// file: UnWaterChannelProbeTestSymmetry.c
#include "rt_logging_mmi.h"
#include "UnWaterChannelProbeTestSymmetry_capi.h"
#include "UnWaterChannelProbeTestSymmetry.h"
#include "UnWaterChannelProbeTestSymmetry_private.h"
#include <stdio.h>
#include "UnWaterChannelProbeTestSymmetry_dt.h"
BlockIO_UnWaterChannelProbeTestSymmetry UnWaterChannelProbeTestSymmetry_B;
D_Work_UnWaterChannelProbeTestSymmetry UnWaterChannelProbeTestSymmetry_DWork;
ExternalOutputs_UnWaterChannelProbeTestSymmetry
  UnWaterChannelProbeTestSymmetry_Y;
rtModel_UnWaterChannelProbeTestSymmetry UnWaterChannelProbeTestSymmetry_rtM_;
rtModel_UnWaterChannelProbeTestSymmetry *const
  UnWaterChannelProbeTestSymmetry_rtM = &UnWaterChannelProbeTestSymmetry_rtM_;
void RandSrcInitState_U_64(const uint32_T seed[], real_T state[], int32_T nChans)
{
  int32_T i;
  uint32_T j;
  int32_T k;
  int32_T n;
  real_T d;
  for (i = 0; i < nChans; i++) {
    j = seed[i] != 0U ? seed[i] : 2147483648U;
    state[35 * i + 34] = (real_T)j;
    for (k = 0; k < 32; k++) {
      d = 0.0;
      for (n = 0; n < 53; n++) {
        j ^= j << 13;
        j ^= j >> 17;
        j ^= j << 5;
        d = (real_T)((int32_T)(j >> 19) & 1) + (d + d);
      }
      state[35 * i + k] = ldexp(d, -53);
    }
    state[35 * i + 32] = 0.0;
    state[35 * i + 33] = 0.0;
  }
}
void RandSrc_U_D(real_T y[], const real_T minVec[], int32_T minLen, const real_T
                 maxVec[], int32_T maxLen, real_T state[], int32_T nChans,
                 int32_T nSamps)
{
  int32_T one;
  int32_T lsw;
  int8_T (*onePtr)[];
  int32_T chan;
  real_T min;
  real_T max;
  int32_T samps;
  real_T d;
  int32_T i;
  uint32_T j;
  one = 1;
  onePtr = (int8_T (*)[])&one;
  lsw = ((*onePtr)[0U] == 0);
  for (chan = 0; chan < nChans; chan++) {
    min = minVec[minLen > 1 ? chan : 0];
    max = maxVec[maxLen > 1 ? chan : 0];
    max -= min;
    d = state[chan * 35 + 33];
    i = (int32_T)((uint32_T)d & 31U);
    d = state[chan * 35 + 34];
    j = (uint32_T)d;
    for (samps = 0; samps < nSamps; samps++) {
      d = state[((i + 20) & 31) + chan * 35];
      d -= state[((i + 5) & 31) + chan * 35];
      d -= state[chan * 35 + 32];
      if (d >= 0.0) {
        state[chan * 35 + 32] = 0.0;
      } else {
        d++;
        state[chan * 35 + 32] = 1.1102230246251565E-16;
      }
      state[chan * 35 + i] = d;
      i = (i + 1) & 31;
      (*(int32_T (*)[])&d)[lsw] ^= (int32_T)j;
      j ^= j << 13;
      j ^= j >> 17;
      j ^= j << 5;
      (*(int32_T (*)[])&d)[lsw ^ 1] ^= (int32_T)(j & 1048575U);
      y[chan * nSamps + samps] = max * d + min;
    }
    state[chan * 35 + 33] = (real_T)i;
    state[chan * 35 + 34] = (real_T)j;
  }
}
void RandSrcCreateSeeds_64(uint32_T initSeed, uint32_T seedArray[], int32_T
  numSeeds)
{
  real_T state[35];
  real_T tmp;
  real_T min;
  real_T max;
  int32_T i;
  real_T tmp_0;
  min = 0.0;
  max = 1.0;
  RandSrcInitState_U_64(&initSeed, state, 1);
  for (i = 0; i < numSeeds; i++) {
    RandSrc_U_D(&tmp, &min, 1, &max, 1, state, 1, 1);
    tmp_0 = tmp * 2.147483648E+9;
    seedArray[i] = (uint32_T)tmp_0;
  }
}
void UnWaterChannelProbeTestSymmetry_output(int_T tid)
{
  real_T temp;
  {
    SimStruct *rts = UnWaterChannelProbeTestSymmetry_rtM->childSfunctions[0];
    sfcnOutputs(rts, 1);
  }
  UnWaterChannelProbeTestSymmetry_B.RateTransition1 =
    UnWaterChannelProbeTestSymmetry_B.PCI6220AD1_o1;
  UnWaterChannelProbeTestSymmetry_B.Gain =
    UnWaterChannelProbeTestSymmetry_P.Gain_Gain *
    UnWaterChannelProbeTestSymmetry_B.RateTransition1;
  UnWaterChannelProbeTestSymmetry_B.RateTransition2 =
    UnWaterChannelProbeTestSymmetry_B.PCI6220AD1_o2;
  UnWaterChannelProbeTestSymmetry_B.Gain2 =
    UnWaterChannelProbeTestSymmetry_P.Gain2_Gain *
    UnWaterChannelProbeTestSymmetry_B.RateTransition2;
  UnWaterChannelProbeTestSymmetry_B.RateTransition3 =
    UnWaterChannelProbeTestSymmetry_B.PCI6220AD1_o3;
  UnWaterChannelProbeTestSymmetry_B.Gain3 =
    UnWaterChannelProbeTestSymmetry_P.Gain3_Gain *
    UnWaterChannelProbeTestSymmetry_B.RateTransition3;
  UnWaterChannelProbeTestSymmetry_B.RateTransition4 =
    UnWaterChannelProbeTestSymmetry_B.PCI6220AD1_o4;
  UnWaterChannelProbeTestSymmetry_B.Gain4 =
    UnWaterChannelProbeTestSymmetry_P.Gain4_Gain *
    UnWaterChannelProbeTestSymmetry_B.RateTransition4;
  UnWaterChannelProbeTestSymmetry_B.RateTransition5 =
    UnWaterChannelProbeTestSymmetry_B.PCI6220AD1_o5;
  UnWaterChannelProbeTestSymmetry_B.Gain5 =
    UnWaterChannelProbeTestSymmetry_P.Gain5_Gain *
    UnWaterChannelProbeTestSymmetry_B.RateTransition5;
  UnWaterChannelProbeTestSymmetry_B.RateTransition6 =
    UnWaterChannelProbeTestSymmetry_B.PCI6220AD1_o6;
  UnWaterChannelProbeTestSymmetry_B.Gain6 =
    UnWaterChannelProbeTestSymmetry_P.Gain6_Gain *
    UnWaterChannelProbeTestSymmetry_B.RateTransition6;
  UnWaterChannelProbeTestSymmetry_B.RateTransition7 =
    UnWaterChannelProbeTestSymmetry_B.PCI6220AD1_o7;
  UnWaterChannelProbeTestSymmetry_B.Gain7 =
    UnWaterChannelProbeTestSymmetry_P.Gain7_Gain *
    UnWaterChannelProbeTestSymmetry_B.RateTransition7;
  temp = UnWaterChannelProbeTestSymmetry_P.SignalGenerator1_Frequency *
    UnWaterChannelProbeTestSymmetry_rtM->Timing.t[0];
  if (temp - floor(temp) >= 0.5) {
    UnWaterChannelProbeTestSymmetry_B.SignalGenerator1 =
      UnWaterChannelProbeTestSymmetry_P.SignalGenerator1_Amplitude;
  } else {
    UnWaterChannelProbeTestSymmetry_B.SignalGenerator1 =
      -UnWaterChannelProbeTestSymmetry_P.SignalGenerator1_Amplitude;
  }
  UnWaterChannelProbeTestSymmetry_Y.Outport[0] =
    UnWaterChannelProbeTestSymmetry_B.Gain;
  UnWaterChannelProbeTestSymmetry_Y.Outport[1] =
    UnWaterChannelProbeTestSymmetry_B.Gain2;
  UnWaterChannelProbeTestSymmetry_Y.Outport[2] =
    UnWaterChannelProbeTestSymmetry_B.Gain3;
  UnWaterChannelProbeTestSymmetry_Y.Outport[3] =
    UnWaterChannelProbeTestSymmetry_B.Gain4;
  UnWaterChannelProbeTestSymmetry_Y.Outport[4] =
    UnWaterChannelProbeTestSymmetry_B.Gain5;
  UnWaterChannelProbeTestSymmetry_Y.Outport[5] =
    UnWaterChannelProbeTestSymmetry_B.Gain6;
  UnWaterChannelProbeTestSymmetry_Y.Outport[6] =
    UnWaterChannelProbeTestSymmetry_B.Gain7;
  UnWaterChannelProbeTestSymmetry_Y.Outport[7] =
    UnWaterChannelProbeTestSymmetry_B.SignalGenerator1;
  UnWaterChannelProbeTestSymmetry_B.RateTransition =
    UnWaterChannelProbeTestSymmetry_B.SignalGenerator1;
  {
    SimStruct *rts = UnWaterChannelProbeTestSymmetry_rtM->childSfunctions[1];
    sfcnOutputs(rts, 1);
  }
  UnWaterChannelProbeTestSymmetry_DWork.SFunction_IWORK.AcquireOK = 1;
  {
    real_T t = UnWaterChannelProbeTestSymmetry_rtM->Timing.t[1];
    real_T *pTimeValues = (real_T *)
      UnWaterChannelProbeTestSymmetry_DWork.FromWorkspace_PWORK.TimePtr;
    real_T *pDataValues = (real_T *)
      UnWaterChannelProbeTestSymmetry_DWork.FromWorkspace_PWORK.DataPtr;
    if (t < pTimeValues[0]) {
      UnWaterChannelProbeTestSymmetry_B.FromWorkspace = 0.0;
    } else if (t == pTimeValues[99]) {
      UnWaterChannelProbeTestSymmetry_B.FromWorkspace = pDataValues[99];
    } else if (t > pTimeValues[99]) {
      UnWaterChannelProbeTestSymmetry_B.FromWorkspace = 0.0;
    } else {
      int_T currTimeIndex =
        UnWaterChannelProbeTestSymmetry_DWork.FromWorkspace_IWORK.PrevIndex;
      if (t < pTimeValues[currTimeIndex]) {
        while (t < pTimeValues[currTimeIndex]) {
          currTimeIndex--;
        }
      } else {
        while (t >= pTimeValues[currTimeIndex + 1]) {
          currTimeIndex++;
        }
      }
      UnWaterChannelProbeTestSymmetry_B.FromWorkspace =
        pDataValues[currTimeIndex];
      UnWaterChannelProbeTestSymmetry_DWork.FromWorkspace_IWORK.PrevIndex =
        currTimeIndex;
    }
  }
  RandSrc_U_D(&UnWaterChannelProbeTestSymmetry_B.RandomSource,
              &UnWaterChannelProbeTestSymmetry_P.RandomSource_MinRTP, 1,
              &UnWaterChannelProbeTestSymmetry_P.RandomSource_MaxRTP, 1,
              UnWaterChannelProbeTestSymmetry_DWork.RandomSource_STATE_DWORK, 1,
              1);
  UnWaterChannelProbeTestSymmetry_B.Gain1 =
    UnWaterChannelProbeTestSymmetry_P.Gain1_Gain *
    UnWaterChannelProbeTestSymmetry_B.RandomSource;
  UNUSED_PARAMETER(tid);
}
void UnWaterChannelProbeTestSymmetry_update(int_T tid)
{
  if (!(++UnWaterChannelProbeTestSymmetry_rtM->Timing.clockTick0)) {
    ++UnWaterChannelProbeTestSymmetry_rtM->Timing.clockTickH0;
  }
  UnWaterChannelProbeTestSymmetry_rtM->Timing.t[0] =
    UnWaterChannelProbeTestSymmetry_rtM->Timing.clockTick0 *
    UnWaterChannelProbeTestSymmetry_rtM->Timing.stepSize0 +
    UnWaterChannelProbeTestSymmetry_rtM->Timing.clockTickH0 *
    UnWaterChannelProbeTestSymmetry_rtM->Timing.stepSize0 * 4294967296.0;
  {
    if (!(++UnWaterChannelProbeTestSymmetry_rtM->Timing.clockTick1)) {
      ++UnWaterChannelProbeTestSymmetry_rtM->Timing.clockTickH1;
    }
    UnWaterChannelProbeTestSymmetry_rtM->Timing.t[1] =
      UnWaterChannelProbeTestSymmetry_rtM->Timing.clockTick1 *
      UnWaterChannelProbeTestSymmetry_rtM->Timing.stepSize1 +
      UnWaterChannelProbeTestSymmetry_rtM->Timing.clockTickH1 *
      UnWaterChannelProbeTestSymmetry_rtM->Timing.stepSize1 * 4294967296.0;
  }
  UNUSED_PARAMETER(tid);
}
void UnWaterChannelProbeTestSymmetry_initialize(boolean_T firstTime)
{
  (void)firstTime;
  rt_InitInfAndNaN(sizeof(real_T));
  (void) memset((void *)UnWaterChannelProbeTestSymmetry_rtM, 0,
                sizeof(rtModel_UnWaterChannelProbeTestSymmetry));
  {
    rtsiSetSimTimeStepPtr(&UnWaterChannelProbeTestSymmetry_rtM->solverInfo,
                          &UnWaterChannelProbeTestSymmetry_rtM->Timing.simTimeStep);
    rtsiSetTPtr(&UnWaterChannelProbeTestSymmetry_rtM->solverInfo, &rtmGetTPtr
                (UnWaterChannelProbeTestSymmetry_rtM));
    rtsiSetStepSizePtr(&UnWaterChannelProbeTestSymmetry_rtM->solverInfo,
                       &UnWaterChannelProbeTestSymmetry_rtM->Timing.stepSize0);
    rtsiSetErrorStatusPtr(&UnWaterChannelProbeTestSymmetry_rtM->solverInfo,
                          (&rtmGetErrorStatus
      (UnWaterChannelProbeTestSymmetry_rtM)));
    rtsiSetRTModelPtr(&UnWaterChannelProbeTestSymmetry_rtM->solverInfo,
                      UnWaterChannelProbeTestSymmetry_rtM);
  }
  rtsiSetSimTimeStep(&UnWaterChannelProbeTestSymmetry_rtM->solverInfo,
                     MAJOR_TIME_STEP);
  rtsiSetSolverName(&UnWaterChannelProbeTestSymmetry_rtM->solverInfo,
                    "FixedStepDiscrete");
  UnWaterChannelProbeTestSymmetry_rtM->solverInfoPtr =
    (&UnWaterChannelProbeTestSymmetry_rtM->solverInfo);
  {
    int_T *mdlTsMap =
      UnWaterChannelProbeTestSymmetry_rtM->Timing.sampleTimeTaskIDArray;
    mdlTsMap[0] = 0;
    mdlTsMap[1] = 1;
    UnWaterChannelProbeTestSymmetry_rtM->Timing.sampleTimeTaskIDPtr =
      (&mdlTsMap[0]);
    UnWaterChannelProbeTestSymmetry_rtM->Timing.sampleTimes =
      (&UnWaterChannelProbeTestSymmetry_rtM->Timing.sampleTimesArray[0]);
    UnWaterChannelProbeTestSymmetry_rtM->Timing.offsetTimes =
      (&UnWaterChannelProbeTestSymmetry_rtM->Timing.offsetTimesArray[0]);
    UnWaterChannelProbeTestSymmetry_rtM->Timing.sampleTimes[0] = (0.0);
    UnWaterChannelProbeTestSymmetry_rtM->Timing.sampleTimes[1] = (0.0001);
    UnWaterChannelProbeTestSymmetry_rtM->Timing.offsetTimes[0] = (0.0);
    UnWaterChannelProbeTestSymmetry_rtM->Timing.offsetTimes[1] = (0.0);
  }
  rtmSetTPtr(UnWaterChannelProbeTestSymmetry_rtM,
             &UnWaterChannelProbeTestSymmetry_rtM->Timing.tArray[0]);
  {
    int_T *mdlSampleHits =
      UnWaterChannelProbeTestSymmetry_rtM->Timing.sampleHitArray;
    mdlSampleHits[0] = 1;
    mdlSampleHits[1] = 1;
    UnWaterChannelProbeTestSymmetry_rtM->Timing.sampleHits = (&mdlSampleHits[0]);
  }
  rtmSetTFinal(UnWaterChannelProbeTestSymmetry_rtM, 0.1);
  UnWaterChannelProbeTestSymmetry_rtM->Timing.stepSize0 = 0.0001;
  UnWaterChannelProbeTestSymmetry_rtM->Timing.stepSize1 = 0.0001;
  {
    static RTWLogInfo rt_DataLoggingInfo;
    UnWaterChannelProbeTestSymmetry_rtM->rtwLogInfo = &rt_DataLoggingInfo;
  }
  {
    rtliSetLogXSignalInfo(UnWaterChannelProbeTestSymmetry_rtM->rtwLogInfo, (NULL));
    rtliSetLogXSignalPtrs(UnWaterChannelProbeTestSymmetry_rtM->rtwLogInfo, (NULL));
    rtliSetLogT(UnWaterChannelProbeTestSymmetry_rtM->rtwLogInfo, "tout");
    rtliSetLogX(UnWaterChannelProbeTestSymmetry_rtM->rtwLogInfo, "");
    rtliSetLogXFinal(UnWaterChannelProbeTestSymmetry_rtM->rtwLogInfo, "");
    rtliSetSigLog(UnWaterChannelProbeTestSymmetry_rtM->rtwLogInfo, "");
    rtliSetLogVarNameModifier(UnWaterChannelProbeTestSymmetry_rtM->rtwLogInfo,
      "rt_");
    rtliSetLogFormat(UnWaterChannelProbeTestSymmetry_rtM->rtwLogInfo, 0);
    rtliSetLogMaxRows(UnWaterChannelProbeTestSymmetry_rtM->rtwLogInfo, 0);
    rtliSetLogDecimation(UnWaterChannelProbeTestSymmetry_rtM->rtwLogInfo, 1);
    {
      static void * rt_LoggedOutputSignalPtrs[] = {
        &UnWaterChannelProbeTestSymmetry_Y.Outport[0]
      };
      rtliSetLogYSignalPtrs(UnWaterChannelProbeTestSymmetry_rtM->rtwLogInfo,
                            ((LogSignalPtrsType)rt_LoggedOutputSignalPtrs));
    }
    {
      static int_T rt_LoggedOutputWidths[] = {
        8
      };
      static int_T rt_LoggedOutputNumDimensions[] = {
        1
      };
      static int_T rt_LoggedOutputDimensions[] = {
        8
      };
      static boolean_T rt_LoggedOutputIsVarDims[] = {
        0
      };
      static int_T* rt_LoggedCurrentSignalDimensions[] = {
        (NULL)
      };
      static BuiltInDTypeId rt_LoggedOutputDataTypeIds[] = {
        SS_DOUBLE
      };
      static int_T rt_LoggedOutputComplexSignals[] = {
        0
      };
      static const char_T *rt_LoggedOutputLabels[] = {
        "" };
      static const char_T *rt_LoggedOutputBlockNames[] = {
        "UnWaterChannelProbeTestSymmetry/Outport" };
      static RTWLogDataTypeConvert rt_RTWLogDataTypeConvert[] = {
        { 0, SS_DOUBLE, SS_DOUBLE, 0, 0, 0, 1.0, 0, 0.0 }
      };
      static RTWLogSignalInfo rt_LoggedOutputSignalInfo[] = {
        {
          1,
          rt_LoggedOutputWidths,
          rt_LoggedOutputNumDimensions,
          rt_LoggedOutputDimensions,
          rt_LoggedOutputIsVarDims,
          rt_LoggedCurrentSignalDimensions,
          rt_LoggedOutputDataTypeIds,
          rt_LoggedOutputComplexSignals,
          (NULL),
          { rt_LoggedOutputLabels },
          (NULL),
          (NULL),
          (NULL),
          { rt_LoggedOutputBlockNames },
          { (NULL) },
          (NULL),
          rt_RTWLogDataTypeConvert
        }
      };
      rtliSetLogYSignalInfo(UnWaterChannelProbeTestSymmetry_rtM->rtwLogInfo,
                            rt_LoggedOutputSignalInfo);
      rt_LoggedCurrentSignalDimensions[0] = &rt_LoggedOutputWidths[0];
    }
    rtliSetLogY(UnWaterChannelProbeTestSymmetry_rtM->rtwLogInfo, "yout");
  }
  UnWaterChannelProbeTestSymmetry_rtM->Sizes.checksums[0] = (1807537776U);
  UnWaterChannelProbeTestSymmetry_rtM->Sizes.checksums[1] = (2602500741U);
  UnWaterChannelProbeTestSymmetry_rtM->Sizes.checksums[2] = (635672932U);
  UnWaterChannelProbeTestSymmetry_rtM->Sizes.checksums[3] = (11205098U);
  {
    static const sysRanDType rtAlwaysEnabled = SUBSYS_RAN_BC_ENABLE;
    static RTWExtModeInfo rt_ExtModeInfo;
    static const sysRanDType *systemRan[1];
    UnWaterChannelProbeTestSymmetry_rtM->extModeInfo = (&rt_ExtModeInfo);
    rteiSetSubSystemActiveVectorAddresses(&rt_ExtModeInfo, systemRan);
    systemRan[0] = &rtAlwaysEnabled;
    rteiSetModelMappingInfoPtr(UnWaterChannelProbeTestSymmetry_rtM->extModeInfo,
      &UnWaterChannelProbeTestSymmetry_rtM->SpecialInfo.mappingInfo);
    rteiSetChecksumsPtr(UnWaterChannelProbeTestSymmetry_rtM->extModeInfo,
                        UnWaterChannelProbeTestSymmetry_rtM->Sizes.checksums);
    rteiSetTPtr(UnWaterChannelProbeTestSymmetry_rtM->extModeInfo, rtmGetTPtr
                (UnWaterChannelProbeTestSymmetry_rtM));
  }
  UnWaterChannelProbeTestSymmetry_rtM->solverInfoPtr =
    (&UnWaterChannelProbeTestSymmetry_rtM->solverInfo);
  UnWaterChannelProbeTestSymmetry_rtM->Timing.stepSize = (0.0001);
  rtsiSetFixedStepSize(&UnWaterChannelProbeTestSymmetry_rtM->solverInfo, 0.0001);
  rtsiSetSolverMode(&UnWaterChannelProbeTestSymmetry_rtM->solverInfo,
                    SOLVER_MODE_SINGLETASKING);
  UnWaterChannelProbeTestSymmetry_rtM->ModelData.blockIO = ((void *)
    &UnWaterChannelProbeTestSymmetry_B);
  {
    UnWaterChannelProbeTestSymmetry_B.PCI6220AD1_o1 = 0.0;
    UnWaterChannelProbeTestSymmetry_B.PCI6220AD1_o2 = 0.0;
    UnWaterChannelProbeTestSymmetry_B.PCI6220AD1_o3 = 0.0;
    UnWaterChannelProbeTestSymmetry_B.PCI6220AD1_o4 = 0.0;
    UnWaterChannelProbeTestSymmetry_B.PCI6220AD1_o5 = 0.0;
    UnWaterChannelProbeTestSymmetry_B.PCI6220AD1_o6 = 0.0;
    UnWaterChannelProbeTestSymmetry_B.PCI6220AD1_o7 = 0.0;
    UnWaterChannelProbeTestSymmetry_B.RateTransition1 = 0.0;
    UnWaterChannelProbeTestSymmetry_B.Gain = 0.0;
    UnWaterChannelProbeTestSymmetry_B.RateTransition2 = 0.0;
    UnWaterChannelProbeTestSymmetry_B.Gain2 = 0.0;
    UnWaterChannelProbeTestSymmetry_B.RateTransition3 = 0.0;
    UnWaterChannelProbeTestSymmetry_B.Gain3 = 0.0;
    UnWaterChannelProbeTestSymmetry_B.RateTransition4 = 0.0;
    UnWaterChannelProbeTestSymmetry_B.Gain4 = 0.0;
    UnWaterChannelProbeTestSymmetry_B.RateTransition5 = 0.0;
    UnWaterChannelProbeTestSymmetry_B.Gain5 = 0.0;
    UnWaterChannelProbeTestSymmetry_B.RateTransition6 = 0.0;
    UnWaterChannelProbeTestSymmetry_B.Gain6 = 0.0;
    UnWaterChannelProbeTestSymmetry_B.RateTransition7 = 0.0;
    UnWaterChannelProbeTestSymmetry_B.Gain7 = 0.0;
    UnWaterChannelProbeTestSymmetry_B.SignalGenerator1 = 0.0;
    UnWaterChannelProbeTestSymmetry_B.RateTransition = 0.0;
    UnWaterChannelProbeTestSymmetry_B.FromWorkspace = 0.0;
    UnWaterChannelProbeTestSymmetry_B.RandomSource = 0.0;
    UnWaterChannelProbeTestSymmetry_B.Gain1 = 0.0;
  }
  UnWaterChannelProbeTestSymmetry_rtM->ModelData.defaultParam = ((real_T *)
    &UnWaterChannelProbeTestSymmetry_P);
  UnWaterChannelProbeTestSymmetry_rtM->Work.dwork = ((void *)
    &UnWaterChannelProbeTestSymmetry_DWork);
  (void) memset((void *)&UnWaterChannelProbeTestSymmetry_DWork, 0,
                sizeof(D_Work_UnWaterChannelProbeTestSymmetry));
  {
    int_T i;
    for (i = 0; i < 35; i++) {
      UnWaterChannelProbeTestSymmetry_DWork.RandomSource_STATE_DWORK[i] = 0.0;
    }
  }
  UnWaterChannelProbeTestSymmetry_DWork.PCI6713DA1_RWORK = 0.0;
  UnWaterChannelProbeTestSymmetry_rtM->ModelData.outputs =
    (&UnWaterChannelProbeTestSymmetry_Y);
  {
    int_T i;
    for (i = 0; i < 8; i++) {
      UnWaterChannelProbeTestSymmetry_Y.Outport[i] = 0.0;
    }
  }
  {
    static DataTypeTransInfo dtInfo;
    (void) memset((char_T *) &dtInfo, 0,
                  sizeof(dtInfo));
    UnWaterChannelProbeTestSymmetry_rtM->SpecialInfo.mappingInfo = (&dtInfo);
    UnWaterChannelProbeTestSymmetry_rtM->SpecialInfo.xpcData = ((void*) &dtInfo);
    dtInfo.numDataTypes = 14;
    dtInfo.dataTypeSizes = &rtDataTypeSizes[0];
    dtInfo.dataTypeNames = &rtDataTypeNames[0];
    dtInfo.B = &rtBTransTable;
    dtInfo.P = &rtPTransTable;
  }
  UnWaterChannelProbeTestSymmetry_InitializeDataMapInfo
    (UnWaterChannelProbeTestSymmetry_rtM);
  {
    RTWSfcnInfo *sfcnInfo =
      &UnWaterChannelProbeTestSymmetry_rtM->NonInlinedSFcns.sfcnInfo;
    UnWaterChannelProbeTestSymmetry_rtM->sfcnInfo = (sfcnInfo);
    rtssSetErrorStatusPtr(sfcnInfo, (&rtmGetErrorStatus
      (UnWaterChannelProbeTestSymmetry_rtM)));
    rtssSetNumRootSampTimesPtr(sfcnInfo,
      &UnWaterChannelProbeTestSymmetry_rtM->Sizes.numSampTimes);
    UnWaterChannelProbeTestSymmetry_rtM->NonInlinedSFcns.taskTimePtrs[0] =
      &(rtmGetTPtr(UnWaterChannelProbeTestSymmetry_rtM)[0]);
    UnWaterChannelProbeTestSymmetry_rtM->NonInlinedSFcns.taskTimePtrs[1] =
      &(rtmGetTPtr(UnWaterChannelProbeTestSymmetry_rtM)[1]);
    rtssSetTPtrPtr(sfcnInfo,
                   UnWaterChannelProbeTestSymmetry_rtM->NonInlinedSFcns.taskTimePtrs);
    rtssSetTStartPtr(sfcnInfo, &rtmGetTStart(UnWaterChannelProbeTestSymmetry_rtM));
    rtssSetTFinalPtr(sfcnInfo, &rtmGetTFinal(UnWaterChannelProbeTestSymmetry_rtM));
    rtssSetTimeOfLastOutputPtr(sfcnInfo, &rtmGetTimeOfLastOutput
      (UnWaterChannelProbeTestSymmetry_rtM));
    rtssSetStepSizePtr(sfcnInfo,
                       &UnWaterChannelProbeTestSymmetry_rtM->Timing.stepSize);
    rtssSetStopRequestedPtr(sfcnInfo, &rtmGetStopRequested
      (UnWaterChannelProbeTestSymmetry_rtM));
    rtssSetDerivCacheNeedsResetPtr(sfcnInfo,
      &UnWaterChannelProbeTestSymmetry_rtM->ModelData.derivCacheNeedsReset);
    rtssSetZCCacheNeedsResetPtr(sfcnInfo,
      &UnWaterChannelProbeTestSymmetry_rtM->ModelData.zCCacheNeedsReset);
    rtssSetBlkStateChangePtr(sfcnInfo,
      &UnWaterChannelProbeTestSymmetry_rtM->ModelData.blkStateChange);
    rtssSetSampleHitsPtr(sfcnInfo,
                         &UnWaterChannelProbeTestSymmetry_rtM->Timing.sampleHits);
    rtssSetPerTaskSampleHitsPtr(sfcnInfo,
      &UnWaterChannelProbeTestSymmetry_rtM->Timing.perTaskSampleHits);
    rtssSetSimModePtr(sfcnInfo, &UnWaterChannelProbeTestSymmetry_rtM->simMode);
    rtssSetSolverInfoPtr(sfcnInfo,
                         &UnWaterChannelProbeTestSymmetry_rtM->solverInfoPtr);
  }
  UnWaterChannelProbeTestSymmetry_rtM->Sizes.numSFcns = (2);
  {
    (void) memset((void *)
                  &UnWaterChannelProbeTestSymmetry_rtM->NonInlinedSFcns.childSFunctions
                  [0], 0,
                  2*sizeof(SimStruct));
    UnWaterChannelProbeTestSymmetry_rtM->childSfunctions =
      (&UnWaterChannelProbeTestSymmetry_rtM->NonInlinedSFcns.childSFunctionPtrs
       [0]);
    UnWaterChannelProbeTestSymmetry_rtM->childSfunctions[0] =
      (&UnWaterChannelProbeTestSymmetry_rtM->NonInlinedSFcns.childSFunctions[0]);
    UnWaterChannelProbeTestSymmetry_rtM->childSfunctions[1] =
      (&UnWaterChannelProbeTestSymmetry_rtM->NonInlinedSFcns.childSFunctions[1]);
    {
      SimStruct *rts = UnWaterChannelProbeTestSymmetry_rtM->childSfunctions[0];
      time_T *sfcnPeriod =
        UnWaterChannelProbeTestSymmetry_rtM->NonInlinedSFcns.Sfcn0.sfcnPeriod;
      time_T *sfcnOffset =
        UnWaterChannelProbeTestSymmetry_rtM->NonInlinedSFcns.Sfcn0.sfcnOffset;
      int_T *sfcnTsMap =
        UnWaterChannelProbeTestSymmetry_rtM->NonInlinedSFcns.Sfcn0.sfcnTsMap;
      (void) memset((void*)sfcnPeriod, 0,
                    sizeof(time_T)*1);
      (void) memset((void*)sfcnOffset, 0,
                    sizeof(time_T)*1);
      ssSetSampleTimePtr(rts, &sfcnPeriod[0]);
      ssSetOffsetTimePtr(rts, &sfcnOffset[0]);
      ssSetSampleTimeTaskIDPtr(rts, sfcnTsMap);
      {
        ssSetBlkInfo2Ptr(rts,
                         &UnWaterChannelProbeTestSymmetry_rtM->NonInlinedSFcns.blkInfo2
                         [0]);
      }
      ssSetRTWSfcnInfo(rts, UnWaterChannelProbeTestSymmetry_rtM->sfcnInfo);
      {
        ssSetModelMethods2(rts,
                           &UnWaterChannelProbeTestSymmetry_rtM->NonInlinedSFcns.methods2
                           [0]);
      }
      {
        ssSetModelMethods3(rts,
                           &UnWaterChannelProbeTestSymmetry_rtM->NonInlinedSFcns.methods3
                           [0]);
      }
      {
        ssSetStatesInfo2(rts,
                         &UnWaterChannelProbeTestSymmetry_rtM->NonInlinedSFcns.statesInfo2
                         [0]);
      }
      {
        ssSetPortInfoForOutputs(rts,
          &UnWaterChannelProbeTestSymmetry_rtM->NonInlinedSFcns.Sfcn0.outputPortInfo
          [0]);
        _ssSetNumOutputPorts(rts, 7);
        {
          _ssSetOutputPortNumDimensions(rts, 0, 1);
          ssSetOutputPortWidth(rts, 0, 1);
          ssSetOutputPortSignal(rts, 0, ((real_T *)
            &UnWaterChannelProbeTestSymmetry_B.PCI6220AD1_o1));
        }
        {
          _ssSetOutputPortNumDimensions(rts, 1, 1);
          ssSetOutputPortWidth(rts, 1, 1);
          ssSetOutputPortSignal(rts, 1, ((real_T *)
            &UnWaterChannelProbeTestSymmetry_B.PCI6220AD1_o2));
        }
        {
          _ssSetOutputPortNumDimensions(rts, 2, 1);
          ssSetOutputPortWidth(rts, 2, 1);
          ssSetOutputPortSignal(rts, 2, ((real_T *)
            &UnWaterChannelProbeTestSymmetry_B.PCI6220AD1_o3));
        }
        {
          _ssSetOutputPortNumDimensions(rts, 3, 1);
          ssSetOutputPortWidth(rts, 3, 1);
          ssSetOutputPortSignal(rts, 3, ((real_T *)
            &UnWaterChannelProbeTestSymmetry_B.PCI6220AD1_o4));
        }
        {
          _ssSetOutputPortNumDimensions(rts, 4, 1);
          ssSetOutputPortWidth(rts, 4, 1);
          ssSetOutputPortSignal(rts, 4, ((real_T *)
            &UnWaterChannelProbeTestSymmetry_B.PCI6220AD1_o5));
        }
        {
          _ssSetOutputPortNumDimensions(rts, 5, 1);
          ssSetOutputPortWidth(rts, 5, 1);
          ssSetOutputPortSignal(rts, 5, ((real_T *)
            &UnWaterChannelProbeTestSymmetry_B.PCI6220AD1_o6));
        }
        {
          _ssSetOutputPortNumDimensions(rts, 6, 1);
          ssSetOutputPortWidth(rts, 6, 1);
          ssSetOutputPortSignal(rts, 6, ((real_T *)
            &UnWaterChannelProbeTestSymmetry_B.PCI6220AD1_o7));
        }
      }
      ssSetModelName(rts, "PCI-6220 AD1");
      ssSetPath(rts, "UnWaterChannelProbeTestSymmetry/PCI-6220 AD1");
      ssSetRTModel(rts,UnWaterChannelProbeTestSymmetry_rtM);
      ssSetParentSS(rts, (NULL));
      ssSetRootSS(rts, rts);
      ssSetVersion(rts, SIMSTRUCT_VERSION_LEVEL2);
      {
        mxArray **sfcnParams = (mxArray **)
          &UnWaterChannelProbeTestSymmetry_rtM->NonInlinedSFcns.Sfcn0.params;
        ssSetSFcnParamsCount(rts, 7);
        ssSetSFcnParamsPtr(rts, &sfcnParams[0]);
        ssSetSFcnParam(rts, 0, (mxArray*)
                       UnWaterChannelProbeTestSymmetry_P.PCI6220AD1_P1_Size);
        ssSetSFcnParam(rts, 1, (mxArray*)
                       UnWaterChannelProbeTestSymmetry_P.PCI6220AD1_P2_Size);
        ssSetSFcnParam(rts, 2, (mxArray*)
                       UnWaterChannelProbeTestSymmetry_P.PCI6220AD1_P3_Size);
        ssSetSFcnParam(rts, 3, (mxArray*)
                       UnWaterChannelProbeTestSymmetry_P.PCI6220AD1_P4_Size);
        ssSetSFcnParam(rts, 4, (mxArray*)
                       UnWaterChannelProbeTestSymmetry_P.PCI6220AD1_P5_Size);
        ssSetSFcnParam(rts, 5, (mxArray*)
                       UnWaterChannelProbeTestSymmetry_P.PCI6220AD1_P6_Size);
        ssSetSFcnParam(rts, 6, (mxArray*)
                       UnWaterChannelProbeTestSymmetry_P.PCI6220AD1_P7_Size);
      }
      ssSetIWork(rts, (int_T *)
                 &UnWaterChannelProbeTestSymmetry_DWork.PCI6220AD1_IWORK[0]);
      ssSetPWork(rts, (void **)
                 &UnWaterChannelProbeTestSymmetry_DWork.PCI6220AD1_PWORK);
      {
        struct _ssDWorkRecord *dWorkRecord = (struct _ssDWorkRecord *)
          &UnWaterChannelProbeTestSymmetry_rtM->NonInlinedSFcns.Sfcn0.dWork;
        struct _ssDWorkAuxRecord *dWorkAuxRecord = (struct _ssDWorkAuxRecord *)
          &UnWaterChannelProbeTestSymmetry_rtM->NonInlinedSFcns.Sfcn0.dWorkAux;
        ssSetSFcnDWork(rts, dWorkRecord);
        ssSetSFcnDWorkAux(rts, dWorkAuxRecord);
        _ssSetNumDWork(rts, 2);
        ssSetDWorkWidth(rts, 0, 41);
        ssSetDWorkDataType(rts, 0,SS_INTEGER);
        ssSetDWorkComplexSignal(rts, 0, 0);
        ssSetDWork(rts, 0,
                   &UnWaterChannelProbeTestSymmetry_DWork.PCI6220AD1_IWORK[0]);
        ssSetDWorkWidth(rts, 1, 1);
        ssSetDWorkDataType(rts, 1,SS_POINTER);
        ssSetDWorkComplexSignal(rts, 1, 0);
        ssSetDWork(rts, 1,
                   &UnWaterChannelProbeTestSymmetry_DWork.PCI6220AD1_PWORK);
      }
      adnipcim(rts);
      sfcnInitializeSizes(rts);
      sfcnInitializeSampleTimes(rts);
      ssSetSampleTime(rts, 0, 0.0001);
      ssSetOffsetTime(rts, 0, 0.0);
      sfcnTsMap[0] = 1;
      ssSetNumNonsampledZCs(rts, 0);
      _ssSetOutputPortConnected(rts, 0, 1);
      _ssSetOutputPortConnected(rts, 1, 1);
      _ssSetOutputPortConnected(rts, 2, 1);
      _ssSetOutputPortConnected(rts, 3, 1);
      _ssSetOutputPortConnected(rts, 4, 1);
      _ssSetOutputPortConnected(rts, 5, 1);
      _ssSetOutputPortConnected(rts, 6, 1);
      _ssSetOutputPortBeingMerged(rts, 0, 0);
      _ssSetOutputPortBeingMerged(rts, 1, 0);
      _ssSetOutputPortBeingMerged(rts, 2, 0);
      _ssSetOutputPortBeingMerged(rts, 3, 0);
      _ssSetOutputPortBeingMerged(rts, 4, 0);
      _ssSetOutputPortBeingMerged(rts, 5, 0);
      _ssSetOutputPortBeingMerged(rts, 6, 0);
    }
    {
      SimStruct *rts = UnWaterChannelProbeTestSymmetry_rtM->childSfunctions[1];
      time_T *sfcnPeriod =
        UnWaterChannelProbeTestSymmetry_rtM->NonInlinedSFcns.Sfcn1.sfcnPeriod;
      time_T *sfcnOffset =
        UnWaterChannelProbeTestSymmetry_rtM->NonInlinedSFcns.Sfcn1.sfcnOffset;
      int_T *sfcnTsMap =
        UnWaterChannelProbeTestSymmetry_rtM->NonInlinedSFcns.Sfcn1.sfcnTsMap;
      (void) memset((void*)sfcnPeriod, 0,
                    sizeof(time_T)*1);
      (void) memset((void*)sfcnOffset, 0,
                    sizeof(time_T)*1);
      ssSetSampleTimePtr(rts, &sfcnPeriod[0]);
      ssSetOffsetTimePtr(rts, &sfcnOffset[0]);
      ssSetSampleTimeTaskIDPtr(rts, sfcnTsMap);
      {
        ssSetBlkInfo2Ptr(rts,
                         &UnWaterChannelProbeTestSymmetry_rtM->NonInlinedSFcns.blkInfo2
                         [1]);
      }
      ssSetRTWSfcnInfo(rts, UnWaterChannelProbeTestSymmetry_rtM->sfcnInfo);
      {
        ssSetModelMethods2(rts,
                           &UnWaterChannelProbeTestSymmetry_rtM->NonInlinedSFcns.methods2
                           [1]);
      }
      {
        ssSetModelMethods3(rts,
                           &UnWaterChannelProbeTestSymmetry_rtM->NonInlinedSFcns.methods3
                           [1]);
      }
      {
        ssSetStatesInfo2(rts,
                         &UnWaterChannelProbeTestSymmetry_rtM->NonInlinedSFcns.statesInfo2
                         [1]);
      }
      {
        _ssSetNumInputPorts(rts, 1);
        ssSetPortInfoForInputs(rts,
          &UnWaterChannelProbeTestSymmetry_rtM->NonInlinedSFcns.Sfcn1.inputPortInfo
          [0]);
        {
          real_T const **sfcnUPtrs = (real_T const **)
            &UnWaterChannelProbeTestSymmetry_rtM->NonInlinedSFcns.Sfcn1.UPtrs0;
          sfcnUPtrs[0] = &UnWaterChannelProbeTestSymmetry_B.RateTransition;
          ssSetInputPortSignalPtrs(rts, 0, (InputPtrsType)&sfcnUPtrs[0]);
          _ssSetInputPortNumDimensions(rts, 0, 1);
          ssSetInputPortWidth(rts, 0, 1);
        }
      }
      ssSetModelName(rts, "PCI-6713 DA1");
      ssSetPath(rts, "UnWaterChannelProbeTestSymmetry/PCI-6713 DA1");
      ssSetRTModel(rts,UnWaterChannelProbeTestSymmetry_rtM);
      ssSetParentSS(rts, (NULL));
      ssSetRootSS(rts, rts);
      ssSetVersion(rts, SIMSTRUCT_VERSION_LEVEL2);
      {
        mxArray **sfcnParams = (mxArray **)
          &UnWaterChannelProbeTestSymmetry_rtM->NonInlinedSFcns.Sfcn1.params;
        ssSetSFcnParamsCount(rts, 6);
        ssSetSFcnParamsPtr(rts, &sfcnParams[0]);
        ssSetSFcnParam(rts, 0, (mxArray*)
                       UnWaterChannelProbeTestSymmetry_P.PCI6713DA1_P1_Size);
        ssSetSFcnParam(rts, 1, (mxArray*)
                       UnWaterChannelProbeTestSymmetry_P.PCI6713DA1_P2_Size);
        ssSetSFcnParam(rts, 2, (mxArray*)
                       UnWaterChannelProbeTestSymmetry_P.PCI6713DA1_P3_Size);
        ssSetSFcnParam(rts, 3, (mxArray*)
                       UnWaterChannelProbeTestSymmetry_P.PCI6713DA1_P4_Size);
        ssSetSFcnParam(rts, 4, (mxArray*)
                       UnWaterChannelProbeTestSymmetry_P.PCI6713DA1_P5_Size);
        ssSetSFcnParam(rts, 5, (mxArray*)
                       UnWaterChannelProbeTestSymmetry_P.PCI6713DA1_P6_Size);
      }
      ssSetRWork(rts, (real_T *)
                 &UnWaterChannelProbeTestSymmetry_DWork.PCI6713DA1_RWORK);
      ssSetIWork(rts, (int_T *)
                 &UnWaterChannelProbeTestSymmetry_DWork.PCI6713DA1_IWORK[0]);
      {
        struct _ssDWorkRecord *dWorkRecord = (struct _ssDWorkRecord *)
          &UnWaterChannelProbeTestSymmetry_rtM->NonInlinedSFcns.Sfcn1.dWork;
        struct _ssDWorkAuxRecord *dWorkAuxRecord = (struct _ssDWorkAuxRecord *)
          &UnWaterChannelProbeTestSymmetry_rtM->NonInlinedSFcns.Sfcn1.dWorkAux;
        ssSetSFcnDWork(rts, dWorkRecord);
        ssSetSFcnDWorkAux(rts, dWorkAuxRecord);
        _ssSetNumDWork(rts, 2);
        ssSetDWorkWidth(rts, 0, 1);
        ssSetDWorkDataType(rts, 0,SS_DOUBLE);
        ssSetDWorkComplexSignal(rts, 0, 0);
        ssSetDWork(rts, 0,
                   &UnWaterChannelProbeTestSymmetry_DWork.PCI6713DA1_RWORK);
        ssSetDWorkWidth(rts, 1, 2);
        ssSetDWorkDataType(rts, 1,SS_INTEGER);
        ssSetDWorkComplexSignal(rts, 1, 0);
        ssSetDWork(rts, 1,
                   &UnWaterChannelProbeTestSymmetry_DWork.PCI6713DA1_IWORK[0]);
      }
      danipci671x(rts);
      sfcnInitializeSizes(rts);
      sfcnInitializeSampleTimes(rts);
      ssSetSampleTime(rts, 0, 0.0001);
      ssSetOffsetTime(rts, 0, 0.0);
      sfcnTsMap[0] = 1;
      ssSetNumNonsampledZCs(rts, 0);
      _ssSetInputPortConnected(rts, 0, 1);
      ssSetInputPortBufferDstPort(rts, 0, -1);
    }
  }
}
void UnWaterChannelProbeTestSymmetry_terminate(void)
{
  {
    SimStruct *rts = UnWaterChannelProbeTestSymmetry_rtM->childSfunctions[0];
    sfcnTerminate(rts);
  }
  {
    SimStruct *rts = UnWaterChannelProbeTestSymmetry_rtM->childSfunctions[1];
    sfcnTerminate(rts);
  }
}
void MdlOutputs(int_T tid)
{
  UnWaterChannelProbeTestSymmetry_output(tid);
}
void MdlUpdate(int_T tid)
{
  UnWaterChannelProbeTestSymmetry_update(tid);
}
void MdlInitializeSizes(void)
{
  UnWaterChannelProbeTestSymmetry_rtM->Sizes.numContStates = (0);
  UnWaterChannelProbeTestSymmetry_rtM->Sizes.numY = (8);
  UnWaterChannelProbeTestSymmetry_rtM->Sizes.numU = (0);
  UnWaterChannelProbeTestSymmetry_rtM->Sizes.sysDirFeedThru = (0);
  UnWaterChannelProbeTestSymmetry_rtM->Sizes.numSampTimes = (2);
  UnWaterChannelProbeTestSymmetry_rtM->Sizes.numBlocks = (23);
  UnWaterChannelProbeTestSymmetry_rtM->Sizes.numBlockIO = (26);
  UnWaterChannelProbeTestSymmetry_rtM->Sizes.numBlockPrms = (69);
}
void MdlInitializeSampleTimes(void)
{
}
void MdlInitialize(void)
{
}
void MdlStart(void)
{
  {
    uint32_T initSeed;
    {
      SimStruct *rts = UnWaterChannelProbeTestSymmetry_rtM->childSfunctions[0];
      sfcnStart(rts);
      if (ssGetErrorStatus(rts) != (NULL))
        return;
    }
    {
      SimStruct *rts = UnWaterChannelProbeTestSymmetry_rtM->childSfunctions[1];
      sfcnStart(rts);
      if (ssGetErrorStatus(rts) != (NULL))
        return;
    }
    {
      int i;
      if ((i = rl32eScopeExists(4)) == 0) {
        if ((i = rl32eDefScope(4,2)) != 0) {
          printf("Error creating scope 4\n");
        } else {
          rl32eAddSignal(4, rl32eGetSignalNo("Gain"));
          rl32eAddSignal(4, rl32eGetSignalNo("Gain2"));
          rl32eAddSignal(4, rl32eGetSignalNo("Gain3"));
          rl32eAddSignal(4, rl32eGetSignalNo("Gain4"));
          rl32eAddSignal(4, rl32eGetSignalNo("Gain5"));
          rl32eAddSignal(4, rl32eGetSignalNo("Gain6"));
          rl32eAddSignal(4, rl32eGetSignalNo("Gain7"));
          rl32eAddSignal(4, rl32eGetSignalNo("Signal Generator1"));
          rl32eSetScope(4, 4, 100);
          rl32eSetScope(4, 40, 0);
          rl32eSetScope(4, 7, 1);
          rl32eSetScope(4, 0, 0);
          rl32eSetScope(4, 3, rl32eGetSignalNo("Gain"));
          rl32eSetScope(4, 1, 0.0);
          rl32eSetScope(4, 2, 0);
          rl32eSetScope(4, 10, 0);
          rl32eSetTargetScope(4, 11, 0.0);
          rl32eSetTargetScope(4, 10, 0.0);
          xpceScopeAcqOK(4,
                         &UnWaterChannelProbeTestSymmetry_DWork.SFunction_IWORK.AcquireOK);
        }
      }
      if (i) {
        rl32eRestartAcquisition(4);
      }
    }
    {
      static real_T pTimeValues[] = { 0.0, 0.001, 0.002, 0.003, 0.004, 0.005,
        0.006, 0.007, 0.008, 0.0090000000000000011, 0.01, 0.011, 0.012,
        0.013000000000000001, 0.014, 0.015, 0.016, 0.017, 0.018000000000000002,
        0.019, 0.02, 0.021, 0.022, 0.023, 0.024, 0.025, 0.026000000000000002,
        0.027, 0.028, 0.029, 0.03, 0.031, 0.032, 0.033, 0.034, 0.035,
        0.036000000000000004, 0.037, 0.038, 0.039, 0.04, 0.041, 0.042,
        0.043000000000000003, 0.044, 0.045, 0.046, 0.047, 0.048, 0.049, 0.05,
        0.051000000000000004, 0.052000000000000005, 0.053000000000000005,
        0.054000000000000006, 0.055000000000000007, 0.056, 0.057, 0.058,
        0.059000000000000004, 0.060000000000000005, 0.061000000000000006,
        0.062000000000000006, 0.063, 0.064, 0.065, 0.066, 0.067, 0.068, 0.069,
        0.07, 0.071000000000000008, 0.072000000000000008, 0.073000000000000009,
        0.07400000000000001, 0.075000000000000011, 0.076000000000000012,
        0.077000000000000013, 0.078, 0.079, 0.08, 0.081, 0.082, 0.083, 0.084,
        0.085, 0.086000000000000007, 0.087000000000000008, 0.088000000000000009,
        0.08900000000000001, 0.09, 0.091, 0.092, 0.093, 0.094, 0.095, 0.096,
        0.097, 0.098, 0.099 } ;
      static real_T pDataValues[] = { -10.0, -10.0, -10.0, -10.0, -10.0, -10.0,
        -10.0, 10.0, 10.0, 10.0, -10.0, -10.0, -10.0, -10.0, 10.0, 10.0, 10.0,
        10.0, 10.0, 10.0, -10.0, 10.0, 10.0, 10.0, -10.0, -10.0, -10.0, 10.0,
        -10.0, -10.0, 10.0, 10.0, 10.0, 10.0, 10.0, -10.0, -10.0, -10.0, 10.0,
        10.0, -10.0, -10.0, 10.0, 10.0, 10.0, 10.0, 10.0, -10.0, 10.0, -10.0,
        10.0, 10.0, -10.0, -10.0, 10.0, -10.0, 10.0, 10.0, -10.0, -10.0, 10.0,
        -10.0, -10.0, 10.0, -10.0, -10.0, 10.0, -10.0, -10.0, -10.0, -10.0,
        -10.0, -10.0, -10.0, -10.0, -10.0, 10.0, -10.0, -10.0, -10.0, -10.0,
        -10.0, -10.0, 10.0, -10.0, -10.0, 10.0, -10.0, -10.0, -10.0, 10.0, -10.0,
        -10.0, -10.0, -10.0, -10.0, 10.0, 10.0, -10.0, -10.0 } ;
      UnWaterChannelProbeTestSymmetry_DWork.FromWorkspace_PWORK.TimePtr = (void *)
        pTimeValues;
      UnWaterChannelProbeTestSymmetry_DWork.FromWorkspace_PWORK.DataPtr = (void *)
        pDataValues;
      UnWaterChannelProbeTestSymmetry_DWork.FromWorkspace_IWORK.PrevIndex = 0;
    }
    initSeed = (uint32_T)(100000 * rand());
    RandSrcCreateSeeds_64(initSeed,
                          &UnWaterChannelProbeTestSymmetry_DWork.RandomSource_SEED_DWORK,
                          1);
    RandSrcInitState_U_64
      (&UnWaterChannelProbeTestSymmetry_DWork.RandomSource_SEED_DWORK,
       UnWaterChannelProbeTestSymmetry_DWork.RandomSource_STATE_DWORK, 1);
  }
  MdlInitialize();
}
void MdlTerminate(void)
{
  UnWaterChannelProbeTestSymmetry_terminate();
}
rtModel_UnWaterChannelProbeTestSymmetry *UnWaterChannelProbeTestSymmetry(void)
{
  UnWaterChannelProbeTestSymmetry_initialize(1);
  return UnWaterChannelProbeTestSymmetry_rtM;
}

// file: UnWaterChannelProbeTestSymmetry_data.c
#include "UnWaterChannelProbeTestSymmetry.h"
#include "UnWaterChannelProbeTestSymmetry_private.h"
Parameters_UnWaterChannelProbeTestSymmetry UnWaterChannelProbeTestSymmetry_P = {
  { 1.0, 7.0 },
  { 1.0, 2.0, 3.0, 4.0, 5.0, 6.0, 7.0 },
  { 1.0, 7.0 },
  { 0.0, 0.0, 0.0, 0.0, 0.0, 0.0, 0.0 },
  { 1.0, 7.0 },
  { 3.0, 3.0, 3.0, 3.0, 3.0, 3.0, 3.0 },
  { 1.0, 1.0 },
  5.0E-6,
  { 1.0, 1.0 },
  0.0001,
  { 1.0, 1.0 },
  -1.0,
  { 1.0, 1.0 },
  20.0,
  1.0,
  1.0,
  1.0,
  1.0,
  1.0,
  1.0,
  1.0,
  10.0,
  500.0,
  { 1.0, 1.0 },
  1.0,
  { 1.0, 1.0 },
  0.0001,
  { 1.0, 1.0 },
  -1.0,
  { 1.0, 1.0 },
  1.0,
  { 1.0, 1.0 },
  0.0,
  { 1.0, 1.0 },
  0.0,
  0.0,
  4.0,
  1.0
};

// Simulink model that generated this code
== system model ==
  Outport : Outport  InitialOutput=0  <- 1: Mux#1
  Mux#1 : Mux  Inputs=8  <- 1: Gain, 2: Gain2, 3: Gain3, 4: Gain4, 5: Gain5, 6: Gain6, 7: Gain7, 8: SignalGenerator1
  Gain : Gain  <- 1: RateTransition1
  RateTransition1 : RateTransition  <- 1: PCI6220AD1
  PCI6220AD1 : S-Function  FunctionName=adnipcim
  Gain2 : Gain  <- 1: RateTransition2
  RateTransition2 : RateTransition  <- 1: PCI6220AD1/2
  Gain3 : Gain  <- 1: RateTransition3
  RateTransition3 : RateTransition  <- 1: PCI6220AD1/3
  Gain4 : Gain  <- 1: RateTransition4
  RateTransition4 : RateTransition  <- 1: PCI6220AD1/4
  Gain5 : Gain  <- 1: RateTransition5
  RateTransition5 : RateTransition  <- 1: PCI6220AD1/5
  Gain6 : Gain  <- 1: RateTransition6
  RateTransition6 : RateTransition  <- 1: PCI6220AD1/6
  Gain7 : Gain  <- 1: RateTransition7
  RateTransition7 : RateTransition  <- 1: PCI6220AD1/7
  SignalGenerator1 : SignalGenerator  Amplitude=10  Frequency=500
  ScopexPC#1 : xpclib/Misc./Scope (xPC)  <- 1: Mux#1
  PCI6713DA1 : xpcnilib/D//A/PCI-6713 DA  <- 1: RateTransition
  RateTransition : RateTransition  <- 1: SignalGenerator1
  FromWorkspace : FromWorkspace
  Gain1 : Gain  <- 1: RandomSource
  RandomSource : dspsrcs4/Random Source
